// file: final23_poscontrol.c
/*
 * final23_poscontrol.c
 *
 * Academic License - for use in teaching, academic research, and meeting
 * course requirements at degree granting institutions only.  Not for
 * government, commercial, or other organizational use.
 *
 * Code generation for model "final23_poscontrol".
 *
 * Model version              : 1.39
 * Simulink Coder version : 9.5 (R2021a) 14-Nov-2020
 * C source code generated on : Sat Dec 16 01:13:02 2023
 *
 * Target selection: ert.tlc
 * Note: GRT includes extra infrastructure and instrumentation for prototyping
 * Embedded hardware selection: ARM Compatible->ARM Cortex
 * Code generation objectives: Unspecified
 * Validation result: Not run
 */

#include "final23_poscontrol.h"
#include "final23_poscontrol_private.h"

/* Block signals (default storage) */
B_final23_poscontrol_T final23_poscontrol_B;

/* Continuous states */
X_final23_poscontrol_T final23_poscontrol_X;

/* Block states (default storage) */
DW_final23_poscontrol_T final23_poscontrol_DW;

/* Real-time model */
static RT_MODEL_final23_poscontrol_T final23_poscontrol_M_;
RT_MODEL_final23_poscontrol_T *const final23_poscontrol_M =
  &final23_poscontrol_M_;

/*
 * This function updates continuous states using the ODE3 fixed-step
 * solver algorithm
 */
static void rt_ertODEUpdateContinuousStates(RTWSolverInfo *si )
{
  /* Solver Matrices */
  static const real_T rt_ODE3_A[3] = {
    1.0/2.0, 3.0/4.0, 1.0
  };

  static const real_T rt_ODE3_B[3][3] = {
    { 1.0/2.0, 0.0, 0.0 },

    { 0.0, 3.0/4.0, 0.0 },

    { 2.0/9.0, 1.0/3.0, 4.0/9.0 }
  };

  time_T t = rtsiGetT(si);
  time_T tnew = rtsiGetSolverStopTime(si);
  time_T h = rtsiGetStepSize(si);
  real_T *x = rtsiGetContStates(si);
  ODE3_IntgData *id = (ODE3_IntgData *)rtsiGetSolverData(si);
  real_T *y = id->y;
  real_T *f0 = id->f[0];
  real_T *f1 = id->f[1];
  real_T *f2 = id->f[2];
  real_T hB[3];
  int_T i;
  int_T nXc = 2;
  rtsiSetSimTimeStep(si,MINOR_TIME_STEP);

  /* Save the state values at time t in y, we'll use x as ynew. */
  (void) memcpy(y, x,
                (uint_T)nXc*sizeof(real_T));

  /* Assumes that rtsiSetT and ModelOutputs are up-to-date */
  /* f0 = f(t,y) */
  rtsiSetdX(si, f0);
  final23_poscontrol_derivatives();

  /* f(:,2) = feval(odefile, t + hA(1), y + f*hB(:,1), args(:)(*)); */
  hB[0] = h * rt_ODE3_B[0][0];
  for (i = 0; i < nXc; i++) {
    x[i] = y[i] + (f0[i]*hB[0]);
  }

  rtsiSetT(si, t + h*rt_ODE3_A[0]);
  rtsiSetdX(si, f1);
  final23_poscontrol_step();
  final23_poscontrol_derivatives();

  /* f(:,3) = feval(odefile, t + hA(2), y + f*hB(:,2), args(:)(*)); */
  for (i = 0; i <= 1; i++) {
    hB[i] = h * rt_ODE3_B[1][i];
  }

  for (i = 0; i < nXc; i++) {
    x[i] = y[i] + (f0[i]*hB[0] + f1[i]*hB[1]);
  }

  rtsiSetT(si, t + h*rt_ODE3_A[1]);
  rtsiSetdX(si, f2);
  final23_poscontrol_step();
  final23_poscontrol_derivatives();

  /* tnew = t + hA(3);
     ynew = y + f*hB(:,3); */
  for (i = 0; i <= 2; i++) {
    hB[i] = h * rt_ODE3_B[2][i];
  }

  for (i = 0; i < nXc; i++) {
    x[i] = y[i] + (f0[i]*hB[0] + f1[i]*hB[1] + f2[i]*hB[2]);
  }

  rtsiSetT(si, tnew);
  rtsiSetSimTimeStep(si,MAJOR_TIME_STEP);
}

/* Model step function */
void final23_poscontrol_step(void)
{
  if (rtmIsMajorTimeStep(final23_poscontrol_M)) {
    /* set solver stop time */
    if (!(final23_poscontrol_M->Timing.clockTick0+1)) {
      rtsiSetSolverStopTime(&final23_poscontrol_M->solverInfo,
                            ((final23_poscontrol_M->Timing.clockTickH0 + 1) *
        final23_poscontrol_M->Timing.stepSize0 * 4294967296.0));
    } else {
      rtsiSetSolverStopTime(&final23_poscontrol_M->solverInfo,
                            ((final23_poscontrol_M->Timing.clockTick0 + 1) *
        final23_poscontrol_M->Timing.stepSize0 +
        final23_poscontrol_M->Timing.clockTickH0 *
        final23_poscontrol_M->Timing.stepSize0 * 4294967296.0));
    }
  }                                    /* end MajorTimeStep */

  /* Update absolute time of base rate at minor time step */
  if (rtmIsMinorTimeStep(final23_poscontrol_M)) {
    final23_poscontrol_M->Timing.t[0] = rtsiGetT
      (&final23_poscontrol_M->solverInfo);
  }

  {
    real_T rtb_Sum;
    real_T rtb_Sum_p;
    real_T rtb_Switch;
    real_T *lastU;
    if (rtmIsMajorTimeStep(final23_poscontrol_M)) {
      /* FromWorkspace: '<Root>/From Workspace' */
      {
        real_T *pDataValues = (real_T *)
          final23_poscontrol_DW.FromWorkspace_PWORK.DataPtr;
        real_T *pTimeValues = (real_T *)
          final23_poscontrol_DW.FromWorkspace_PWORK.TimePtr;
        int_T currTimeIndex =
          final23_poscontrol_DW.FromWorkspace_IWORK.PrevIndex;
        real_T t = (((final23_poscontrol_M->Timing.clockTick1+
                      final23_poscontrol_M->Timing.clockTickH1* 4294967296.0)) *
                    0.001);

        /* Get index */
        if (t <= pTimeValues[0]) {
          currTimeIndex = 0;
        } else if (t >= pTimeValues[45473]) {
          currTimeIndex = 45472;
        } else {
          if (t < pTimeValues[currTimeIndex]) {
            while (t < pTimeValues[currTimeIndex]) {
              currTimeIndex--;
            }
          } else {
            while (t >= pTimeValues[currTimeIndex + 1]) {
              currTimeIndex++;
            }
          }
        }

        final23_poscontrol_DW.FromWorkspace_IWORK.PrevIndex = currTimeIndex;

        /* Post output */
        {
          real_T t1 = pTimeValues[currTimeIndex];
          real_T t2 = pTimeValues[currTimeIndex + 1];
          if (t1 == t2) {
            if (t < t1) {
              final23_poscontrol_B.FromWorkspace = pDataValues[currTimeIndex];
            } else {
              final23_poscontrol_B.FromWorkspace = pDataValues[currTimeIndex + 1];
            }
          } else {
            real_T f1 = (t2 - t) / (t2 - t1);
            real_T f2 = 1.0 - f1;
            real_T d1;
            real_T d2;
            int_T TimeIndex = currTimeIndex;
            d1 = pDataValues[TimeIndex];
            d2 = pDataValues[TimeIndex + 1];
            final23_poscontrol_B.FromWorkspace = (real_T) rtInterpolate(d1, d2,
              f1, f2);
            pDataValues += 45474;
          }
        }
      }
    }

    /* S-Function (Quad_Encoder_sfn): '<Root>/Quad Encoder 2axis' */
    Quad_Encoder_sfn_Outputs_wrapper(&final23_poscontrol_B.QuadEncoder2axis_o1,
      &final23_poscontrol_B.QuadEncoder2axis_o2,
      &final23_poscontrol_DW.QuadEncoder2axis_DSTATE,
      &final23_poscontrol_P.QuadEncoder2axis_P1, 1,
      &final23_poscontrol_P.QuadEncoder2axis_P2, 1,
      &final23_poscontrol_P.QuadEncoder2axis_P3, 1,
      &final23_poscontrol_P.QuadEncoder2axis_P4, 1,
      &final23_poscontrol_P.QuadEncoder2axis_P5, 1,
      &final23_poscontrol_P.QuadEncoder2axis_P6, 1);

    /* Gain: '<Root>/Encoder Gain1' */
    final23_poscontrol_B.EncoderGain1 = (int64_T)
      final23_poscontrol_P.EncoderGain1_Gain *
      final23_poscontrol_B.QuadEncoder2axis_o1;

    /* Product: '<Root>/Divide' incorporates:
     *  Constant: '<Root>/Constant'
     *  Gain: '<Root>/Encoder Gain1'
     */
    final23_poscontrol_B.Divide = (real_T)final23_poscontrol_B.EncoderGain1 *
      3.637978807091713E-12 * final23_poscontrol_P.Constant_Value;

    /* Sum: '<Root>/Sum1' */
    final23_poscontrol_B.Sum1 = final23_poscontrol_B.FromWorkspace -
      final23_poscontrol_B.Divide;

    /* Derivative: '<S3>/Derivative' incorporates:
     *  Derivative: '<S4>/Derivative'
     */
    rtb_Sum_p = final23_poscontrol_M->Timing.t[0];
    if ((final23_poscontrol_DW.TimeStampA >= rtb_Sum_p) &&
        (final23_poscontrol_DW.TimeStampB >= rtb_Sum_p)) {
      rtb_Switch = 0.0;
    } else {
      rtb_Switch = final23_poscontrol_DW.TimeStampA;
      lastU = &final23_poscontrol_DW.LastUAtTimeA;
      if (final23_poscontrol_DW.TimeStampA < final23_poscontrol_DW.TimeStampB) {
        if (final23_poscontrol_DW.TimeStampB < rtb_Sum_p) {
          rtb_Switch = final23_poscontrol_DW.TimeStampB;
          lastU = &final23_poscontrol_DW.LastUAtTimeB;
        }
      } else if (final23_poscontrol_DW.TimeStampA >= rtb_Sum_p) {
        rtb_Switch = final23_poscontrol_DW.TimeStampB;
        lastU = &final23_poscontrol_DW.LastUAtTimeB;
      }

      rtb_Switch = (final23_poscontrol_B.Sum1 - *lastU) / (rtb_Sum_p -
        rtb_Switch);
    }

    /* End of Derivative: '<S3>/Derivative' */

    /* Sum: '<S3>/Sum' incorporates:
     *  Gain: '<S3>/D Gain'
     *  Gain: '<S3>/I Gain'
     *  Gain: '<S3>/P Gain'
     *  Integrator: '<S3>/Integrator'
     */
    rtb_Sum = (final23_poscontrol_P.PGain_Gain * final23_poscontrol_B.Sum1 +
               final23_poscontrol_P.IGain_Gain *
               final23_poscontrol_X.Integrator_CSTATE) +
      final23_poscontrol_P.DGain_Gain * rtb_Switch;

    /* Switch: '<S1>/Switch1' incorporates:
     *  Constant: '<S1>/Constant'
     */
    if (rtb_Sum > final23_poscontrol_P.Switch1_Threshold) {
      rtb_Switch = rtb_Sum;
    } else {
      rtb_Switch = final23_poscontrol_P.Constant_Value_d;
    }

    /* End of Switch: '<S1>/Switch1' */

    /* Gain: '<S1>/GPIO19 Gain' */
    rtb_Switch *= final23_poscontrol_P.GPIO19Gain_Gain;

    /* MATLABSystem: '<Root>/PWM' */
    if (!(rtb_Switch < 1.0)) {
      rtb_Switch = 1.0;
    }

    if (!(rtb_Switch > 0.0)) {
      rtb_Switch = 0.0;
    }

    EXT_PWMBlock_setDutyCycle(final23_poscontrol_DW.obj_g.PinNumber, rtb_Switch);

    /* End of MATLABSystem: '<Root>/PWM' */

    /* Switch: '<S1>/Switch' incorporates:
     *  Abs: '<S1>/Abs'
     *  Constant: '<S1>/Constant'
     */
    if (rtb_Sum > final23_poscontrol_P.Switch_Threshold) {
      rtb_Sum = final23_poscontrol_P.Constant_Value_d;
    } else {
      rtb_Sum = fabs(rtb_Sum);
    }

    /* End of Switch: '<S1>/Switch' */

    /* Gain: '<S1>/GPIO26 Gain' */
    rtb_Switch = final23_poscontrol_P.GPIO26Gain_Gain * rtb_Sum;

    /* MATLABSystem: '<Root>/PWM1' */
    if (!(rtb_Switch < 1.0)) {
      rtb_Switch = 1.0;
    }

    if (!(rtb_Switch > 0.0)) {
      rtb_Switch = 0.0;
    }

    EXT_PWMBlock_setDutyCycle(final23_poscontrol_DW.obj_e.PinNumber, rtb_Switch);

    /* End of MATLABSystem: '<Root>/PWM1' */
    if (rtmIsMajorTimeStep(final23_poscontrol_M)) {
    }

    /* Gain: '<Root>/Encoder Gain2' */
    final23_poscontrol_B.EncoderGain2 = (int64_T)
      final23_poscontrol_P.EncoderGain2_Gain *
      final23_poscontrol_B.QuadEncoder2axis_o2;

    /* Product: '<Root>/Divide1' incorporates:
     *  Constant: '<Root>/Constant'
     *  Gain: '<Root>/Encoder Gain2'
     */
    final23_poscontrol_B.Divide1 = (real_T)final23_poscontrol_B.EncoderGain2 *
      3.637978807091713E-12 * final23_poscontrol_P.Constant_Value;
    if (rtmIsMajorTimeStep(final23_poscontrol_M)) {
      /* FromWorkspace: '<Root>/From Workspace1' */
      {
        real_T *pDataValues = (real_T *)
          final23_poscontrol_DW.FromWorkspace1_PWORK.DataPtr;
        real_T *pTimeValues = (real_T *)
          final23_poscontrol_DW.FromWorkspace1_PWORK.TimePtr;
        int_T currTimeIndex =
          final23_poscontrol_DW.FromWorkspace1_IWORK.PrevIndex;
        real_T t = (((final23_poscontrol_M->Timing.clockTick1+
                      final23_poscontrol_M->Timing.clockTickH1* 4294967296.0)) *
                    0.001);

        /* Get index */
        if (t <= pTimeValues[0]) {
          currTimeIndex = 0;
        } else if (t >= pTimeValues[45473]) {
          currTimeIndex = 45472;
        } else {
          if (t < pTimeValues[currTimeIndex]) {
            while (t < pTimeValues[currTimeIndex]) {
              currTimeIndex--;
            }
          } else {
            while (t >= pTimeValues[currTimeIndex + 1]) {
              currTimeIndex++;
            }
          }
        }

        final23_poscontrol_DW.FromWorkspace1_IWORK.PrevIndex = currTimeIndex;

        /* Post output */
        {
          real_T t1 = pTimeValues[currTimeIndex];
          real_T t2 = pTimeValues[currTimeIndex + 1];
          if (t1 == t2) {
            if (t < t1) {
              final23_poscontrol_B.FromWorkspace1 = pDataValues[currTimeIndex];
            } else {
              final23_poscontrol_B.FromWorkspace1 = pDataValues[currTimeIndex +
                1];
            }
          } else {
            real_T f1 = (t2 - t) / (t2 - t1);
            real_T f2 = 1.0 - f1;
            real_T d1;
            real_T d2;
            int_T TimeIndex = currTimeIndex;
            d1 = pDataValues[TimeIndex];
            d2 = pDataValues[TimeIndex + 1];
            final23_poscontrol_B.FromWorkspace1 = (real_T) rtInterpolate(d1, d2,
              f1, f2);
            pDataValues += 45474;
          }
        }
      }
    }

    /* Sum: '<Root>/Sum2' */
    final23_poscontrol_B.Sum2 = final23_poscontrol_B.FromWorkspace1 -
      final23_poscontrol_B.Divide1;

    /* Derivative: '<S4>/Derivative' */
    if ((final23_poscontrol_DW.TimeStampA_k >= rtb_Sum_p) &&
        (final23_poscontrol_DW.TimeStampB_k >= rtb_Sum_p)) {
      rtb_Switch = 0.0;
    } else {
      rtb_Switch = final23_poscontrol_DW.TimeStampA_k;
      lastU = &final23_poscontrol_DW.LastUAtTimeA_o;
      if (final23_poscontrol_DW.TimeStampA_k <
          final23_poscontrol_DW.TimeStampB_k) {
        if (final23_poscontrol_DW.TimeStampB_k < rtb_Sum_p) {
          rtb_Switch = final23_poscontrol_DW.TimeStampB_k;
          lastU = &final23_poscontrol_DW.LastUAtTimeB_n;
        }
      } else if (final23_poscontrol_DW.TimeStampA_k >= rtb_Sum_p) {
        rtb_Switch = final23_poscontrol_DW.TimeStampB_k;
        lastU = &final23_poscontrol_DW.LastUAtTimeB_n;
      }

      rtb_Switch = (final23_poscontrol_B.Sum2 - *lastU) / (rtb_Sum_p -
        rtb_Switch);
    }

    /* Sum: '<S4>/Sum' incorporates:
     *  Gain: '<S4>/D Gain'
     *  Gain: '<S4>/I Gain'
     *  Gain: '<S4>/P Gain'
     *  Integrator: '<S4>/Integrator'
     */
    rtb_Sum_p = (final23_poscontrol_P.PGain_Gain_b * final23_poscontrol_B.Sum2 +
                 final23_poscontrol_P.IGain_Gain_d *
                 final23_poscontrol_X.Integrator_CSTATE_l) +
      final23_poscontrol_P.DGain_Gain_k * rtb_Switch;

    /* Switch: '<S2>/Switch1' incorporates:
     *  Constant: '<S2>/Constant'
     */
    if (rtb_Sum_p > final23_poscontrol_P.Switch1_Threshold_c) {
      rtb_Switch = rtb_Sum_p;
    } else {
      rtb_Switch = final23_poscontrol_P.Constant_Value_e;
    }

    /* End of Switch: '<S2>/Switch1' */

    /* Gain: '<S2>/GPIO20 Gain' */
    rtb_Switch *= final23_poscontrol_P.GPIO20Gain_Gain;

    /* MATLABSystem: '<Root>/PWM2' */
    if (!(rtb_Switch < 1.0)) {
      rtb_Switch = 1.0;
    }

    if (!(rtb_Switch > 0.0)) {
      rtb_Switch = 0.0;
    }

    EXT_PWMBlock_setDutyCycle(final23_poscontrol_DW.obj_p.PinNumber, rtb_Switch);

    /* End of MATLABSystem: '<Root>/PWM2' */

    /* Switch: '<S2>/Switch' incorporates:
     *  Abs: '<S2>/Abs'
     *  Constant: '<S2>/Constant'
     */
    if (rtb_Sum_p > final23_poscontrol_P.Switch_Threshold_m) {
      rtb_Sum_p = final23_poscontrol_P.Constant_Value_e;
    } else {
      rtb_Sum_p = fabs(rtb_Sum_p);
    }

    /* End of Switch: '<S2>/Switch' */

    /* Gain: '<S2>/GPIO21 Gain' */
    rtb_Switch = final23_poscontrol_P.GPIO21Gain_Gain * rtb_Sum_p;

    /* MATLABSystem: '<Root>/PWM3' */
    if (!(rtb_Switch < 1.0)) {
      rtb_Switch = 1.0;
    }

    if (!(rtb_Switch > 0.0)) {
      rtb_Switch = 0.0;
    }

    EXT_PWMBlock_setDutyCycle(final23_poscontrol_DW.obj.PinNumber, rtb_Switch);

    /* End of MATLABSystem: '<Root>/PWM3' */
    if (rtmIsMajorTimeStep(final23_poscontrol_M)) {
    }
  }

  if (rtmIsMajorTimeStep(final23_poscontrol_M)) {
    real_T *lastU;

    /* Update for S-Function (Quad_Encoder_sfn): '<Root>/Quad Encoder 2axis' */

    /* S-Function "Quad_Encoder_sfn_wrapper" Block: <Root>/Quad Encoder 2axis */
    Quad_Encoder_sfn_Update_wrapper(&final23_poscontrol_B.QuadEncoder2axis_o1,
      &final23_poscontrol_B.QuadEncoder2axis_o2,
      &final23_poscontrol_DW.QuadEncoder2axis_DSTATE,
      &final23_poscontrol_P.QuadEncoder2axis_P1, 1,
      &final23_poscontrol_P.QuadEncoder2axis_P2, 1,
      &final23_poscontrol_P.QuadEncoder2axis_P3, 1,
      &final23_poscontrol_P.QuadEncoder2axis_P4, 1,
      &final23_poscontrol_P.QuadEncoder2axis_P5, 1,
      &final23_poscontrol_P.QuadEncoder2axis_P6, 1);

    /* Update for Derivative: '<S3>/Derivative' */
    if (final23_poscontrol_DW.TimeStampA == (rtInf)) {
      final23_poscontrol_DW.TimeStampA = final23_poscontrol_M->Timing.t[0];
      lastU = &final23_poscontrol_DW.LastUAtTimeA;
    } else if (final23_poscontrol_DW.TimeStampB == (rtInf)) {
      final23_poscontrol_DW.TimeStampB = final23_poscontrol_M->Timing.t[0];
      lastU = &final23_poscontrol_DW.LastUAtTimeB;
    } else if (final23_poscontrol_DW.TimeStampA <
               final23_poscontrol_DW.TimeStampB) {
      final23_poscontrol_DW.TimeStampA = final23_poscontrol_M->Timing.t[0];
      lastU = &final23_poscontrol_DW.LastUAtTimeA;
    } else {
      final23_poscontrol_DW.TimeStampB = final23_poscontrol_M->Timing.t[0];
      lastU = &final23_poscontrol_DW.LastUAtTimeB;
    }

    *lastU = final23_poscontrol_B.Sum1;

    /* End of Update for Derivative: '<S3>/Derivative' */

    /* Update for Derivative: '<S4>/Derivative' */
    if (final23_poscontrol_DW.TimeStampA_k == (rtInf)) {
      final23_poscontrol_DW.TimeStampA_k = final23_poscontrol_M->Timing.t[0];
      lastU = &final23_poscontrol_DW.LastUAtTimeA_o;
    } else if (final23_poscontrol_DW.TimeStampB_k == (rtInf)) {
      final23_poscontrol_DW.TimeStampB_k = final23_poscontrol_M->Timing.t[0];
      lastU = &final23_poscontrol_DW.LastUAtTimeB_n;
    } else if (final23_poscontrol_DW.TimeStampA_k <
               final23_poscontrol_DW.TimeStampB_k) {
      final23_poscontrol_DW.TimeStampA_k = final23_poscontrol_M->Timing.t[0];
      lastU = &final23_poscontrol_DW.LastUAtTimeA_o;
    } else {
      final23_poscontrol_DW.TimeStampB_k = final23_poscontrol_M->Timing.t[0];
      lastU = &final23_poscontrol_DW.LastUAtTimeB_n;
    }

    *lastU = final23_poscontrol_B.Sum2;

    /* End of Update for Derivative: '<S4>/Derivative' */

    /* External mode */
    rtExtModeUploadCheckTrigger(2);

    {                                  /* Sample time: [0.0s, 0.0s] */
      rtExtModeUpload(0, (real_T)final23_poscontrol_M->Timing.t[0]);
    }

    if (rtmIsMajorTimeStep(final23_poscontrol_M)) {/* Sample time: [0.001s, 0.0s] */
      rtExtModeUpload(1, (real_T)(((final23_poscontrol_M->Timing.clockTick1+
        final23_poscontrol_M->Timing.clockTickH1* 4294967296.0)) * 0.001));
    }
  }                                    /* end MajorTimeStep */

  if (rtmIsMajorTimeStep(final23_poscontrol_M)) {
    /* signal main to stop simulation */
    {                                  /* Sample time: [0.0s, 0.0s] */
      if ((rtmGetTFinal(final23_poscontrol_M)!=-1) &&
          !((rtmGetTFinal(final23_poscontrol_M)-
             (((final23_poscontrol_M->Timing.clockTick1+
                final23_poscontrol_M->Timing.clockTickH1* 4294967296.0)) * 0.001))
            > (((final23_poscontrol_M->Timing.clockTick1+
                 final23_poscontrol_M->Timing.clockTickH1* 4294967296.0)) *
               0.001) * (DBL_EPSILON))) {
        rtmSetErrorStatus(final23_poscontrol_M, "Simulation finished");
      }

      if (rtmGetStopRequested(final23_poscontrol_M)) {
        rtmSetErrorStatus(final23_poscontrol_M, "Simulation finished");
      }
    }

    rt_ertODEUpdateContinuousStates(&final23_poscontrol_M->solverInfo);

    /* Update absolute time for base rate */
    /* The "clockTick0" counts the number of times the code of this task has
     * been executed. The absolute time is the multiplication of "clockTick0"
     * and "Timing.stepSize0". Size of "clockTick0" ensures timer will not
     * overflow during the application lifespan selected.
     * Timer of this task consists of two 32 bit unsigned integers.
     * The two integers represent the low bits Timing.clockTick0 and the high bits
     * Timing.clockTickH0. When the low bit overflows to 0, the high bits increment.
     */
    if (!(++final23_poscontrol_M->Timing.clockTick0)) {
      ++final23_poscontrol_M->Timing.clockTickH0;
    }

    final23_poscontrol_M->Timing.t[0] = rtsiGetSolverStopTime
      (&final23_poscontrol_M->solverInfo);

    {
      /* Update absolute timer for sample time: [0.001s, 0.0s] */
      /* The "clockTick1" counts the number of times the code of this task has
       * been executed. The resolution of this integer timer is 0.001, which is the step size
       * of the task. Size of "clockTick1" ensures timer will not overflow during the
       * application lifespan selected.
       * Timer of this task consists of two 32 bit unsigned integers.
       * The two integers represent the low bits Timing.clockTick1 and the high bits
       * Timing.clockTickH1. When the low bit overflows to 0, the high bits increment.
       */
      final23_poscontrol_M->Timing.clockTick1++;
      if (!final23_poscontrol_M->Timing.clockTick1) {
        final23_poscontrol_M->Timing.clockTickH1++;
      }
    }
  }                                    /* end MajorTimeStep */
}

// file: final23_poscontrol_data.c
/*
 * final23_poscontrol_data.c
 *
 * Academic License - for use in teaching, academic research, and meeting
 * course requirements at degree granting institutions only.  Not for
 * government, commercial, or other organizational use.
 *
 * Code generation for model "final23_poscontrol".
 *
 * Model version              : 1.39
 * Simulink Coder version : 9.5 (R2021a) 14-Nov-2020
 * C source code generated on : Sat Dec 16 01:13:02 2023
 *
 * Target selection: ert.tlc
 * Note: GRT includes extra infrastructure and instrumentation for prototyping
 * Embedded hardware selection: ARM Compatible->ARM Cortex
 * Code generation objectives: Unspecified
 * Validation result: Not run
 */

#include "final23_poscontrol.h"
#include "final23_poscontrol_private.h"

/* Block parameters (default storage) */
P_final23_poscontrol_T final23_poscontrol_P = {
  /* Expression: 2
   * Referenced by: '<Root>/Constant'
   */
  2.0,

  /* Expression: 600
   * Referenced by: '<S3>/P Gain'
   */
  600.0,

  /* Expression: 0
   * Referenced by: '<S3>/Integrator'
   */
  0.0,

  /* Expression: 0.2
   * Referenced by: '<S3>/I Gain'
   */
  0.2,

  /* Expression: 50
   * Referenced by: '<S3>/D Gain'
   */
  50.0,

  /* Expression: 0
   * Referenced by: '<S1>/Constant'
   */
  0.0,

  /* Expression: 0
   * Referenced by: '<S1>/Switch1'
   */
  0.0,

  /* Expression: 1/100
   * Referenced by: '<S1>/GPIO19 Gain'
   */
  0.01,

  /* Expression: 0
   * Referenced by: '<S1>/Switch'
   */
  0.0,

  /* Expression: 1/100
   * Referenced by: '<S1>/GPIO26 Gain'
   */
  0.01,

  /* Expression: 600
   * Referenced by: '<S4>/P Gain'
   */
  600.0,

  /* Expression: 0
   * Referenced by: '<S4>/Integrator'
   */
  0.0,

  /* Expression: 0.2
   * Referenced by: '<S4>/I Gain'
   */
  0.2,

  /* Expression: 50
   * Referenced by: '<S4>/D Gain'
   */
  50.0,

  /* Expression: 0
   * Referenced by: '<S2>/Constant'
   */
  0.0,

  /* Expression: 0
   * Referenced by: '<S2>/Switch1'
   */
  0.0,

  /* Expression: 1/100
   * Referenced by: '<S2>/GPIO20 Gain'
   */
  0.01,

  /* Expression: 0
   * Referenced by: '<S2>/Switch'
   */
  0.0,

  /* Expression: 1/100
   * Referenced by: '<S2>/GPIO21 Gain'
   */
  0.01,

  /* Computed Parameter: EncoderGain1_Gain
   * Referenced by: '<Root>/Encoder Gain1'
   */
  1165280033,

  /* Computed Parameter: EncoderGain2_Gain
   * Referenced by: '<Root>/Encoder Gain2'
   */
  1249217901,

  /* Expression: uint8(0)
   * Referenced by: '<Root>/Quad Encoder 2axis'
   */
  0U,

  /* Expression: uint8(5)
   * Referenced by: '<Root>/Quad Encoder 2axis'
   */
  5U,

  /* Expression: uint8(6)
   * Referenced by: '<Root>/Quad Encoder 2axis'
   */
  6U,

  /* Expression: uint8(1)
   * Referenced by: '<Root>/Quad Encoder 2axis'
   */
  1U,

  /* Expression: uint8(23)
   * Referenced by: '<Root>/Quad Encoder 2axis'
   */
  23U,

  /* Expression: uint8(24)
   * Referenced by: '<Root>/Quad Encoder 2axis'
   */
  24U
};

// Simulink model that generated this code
simulink model "final23_poscontrol"  (R2021a)
settings: Solver=FixedStepAuto  StartTime=0.0  StopTime=45  FixedStep=0.001  RelTol=1e-3  EnableMultiTasking=on
StopFcn:
  | mypi=raspi();
  | writeDigitalPin(mypi,19,0);
  | writeDigitalPin(mypi,26,0);
  | writeDigitalPin(mypi,20,0);
  | writeDigitalPin(mypi,21,0);
  | clear mypi;
libraries: raspberrypiBasiclib x4

== system final23_poscontrol ==
  Constant : Constant  Value=2
  Divide : Product  Inputs=**
  Divide1 : Product  Inputs=**
  Encoder Gain1 : Gain  Gain=1/235.89
  Encoder Gain2 : Gain  Gain=1/220.04
  From Workspace : FromWorkspace  VariableName=xInput  SampleTime=0.001
  From Workspace1 : FromWorkspace  VariableName=yInput  SampleTime=0.001
  Motor Subsystem : Subsystem
  Motor Subsystem1 : Subsystem
  PID Subsystem : Subsystem
  PID Subsystem1 : Subsystem
  PWM : raspberrypiBasiclib/PWM  board=Pi 4 Model B  Pin_=19  Frequency=1000  blockPlatform=Raspberry Pi
  PWM1 : raspberrypiBasiclib/PWM  board=Pi 4 Model B  Pin_=26  Frequency=1000  blockPlatform=Raspberry Pi
  PWM2 : raspberrypiBasiclib/PWM  board=Pi 4 Model B  Pin_=20  Frequency=1000  blockPlatform=Raspberry Pi
  PWM3 : raspberrypiBasiclib/PWM  board=Pi 4 Model B  Pin_=21  Frequency=1000  blockPlatform=Raspberry Pi
  Quad Encoder 2axis : S-Function  InitFcn=try, set_param(gcb,'FunctionName','Quad_Encoder_sfn'), end  FunctionName=Quad_Encoder_sfn  Parameters=uint8(0),uint8(5),uint8(6),uint8(1),uint8(23),uint8(24)  SFunctionModules=Quad_Encoder_sfn_wrapper  SFunctionDeploymentMode=off  EnableBusSupport=off  mask(S-Function Builder){}
      mask init:
      | val = [[.9  0.75 0.75 1 1 .9 .9 1]',[1 1 0.75 0.75 .9 .9 1 .9]'];try , sys = get_param(gcb,'SfunBuilderFcnName');if isempty(sys), sys = get_param(gcb,'FunctionName'); end,catch, sys = get_param(gcb,'FunctionName'); end
  Sum1 : Sum  Inputs=|+-
  Sum2 : Sum  Inputs=-+|
  To Workspace1 : ToWorkspace  VariableName=xpos  SampleTime=0.001
  To Workspace2 : ToWorkspace  VariableName=ypos  SampleTime=0.001
  wires:
  Quad Encoder 2axis/1 -> Encoder Gain1/1
  Quad Encoder 2axis/2 -> Encoder Gain2/1
  Sum1/1 -> PID Subsystem/1(In1)
  PID Subsystem/1(Out1) -> Motor Subsystem/1(In1)
  Motor Subsystem/1(Out1) -> PWM/1
  Motor Subsystem/2(Out2) -> PWM1/1
  Motor Subsystem1/2(Out2) -> PWM3/1
  Motor Subsystem1/1(Out1) -> PWM2/1
  PID Subsystem1/1(Out1) -> Motor Subsystem1/1(In1)
  Sum2/1 -> PID Subsystem1/1(In1)
  From Workspace/1 -> Sum1/1
  From Workspace1/1 -> Sum2/2
  Encoder Gain1/1 -> Divide/1
  Encoder Gain2/1 -> Divide1/2
  Divide1/1 -> To Workspace2/1, Sum2/1
  Divide/1 -> Sum1/2, To Workspace1/1
  Constant/1 -> Divide1/1, Divide/2

== system final23_poscontrol/Motor Subsystem ==
  In1 : Inport
  Abs : Abs
  Constant : Constant  Value=0
  GPIO19 Gain : Gain  Gain=1/100
  GPIO26 Gain : Gain  Gain=1/100
  Switch : Switch  Criteria=u2 > Threshold
  Switch1 : Switch  Criteria=u2 > Threshold
  Out1 : Outport
  Out2 : Outport  Port=2
  wires:
  Switch/1 -> GPIO26 Gain/1
  Abs/1 -> Switch/3
  Switch1/1 -> GPIO19 Gain/1
  In1/1 -> Abs/1, Switch/2, Switch1/1, Switch1/2
  Constant/1 -> Switch/1, Switch1/3
  GPIO26 Gain/1 -> Out2/1
  GPIO19 Gain/1 -> Out1/1

== system final23_poscontrol/Motor Subsystem1 ==
  In1 : Inport
  Abs : Abs
  Constant : Constant  Value=0
  GPIO20 Gain : Gain  Gain=1/100
  GPIO21 Gain : Gain  Gain=1/100
  Switch : Switch  Criteria=u2 > Threshold
  Switch1 : Switch  Criteria=u2 > Threshold
  Out1 : Outport
  Out2 : Outport  Port=2
  wires:
  Switch/1 -> GPIO21 Gain/1
  Abs/1 -> Switch/3
  Switch1/1 -> GPIO20 Gain/1
  In1/1 -> Abs/1, Switch/2, Switch1/1, Switch1/2
  Constant/1 -> Switch/1, Switch1/3
  GPIO21 Gain/1 -> Out2/1
  GPIO20 Gain/1 -> Out1/1

== system final23_poscontrol/PID Subsystem ==
  In1 : Inport
  D Gain : Gain  Gain=50
  Derivative : Derivative
  I Gain : Gain  Gain=0.2
  Integrator : Integrator
  P Gain : Gain  Gain=600
  Sum : Sum  Inputs=+++
  Out1 : Outport
  wires:
  Derivative/1 -> D Gain/1
  I Gain/1 -> Sum/2
  Integrator/1 -> I Gain/1
  P Gain/1 -> Sum/1
  D Gain/1 -> Sum/3
  Sum/1 -> Out1/1
  In1/1 -> P Gain/1, Derivative/1, Integrator/1

== system final23_poscontrol/PID Subsystem1 ==
  In1 : Inport
  D Gain : Gain  Gain=50
  Derivative : Derivative
  I Gain : Gain  Gain=0.2
  Integrator : Integrator
  P Gain : Gain  Gain=600
  Sum : Sum  Inputs=+++
  Out1 : Outport
  wires:
  Derivative/1 -> D Gain/1
  I Gain/1 -> Sum/2
  Integrator/1 -> I Gain/1
  P Gain/1 -> Sum/1
  D Gain/1 -> Sum/3
  Sum/1 -> Out1/1
  In1/1 -> P Gain/1, Derivative/1, Integrator/1
